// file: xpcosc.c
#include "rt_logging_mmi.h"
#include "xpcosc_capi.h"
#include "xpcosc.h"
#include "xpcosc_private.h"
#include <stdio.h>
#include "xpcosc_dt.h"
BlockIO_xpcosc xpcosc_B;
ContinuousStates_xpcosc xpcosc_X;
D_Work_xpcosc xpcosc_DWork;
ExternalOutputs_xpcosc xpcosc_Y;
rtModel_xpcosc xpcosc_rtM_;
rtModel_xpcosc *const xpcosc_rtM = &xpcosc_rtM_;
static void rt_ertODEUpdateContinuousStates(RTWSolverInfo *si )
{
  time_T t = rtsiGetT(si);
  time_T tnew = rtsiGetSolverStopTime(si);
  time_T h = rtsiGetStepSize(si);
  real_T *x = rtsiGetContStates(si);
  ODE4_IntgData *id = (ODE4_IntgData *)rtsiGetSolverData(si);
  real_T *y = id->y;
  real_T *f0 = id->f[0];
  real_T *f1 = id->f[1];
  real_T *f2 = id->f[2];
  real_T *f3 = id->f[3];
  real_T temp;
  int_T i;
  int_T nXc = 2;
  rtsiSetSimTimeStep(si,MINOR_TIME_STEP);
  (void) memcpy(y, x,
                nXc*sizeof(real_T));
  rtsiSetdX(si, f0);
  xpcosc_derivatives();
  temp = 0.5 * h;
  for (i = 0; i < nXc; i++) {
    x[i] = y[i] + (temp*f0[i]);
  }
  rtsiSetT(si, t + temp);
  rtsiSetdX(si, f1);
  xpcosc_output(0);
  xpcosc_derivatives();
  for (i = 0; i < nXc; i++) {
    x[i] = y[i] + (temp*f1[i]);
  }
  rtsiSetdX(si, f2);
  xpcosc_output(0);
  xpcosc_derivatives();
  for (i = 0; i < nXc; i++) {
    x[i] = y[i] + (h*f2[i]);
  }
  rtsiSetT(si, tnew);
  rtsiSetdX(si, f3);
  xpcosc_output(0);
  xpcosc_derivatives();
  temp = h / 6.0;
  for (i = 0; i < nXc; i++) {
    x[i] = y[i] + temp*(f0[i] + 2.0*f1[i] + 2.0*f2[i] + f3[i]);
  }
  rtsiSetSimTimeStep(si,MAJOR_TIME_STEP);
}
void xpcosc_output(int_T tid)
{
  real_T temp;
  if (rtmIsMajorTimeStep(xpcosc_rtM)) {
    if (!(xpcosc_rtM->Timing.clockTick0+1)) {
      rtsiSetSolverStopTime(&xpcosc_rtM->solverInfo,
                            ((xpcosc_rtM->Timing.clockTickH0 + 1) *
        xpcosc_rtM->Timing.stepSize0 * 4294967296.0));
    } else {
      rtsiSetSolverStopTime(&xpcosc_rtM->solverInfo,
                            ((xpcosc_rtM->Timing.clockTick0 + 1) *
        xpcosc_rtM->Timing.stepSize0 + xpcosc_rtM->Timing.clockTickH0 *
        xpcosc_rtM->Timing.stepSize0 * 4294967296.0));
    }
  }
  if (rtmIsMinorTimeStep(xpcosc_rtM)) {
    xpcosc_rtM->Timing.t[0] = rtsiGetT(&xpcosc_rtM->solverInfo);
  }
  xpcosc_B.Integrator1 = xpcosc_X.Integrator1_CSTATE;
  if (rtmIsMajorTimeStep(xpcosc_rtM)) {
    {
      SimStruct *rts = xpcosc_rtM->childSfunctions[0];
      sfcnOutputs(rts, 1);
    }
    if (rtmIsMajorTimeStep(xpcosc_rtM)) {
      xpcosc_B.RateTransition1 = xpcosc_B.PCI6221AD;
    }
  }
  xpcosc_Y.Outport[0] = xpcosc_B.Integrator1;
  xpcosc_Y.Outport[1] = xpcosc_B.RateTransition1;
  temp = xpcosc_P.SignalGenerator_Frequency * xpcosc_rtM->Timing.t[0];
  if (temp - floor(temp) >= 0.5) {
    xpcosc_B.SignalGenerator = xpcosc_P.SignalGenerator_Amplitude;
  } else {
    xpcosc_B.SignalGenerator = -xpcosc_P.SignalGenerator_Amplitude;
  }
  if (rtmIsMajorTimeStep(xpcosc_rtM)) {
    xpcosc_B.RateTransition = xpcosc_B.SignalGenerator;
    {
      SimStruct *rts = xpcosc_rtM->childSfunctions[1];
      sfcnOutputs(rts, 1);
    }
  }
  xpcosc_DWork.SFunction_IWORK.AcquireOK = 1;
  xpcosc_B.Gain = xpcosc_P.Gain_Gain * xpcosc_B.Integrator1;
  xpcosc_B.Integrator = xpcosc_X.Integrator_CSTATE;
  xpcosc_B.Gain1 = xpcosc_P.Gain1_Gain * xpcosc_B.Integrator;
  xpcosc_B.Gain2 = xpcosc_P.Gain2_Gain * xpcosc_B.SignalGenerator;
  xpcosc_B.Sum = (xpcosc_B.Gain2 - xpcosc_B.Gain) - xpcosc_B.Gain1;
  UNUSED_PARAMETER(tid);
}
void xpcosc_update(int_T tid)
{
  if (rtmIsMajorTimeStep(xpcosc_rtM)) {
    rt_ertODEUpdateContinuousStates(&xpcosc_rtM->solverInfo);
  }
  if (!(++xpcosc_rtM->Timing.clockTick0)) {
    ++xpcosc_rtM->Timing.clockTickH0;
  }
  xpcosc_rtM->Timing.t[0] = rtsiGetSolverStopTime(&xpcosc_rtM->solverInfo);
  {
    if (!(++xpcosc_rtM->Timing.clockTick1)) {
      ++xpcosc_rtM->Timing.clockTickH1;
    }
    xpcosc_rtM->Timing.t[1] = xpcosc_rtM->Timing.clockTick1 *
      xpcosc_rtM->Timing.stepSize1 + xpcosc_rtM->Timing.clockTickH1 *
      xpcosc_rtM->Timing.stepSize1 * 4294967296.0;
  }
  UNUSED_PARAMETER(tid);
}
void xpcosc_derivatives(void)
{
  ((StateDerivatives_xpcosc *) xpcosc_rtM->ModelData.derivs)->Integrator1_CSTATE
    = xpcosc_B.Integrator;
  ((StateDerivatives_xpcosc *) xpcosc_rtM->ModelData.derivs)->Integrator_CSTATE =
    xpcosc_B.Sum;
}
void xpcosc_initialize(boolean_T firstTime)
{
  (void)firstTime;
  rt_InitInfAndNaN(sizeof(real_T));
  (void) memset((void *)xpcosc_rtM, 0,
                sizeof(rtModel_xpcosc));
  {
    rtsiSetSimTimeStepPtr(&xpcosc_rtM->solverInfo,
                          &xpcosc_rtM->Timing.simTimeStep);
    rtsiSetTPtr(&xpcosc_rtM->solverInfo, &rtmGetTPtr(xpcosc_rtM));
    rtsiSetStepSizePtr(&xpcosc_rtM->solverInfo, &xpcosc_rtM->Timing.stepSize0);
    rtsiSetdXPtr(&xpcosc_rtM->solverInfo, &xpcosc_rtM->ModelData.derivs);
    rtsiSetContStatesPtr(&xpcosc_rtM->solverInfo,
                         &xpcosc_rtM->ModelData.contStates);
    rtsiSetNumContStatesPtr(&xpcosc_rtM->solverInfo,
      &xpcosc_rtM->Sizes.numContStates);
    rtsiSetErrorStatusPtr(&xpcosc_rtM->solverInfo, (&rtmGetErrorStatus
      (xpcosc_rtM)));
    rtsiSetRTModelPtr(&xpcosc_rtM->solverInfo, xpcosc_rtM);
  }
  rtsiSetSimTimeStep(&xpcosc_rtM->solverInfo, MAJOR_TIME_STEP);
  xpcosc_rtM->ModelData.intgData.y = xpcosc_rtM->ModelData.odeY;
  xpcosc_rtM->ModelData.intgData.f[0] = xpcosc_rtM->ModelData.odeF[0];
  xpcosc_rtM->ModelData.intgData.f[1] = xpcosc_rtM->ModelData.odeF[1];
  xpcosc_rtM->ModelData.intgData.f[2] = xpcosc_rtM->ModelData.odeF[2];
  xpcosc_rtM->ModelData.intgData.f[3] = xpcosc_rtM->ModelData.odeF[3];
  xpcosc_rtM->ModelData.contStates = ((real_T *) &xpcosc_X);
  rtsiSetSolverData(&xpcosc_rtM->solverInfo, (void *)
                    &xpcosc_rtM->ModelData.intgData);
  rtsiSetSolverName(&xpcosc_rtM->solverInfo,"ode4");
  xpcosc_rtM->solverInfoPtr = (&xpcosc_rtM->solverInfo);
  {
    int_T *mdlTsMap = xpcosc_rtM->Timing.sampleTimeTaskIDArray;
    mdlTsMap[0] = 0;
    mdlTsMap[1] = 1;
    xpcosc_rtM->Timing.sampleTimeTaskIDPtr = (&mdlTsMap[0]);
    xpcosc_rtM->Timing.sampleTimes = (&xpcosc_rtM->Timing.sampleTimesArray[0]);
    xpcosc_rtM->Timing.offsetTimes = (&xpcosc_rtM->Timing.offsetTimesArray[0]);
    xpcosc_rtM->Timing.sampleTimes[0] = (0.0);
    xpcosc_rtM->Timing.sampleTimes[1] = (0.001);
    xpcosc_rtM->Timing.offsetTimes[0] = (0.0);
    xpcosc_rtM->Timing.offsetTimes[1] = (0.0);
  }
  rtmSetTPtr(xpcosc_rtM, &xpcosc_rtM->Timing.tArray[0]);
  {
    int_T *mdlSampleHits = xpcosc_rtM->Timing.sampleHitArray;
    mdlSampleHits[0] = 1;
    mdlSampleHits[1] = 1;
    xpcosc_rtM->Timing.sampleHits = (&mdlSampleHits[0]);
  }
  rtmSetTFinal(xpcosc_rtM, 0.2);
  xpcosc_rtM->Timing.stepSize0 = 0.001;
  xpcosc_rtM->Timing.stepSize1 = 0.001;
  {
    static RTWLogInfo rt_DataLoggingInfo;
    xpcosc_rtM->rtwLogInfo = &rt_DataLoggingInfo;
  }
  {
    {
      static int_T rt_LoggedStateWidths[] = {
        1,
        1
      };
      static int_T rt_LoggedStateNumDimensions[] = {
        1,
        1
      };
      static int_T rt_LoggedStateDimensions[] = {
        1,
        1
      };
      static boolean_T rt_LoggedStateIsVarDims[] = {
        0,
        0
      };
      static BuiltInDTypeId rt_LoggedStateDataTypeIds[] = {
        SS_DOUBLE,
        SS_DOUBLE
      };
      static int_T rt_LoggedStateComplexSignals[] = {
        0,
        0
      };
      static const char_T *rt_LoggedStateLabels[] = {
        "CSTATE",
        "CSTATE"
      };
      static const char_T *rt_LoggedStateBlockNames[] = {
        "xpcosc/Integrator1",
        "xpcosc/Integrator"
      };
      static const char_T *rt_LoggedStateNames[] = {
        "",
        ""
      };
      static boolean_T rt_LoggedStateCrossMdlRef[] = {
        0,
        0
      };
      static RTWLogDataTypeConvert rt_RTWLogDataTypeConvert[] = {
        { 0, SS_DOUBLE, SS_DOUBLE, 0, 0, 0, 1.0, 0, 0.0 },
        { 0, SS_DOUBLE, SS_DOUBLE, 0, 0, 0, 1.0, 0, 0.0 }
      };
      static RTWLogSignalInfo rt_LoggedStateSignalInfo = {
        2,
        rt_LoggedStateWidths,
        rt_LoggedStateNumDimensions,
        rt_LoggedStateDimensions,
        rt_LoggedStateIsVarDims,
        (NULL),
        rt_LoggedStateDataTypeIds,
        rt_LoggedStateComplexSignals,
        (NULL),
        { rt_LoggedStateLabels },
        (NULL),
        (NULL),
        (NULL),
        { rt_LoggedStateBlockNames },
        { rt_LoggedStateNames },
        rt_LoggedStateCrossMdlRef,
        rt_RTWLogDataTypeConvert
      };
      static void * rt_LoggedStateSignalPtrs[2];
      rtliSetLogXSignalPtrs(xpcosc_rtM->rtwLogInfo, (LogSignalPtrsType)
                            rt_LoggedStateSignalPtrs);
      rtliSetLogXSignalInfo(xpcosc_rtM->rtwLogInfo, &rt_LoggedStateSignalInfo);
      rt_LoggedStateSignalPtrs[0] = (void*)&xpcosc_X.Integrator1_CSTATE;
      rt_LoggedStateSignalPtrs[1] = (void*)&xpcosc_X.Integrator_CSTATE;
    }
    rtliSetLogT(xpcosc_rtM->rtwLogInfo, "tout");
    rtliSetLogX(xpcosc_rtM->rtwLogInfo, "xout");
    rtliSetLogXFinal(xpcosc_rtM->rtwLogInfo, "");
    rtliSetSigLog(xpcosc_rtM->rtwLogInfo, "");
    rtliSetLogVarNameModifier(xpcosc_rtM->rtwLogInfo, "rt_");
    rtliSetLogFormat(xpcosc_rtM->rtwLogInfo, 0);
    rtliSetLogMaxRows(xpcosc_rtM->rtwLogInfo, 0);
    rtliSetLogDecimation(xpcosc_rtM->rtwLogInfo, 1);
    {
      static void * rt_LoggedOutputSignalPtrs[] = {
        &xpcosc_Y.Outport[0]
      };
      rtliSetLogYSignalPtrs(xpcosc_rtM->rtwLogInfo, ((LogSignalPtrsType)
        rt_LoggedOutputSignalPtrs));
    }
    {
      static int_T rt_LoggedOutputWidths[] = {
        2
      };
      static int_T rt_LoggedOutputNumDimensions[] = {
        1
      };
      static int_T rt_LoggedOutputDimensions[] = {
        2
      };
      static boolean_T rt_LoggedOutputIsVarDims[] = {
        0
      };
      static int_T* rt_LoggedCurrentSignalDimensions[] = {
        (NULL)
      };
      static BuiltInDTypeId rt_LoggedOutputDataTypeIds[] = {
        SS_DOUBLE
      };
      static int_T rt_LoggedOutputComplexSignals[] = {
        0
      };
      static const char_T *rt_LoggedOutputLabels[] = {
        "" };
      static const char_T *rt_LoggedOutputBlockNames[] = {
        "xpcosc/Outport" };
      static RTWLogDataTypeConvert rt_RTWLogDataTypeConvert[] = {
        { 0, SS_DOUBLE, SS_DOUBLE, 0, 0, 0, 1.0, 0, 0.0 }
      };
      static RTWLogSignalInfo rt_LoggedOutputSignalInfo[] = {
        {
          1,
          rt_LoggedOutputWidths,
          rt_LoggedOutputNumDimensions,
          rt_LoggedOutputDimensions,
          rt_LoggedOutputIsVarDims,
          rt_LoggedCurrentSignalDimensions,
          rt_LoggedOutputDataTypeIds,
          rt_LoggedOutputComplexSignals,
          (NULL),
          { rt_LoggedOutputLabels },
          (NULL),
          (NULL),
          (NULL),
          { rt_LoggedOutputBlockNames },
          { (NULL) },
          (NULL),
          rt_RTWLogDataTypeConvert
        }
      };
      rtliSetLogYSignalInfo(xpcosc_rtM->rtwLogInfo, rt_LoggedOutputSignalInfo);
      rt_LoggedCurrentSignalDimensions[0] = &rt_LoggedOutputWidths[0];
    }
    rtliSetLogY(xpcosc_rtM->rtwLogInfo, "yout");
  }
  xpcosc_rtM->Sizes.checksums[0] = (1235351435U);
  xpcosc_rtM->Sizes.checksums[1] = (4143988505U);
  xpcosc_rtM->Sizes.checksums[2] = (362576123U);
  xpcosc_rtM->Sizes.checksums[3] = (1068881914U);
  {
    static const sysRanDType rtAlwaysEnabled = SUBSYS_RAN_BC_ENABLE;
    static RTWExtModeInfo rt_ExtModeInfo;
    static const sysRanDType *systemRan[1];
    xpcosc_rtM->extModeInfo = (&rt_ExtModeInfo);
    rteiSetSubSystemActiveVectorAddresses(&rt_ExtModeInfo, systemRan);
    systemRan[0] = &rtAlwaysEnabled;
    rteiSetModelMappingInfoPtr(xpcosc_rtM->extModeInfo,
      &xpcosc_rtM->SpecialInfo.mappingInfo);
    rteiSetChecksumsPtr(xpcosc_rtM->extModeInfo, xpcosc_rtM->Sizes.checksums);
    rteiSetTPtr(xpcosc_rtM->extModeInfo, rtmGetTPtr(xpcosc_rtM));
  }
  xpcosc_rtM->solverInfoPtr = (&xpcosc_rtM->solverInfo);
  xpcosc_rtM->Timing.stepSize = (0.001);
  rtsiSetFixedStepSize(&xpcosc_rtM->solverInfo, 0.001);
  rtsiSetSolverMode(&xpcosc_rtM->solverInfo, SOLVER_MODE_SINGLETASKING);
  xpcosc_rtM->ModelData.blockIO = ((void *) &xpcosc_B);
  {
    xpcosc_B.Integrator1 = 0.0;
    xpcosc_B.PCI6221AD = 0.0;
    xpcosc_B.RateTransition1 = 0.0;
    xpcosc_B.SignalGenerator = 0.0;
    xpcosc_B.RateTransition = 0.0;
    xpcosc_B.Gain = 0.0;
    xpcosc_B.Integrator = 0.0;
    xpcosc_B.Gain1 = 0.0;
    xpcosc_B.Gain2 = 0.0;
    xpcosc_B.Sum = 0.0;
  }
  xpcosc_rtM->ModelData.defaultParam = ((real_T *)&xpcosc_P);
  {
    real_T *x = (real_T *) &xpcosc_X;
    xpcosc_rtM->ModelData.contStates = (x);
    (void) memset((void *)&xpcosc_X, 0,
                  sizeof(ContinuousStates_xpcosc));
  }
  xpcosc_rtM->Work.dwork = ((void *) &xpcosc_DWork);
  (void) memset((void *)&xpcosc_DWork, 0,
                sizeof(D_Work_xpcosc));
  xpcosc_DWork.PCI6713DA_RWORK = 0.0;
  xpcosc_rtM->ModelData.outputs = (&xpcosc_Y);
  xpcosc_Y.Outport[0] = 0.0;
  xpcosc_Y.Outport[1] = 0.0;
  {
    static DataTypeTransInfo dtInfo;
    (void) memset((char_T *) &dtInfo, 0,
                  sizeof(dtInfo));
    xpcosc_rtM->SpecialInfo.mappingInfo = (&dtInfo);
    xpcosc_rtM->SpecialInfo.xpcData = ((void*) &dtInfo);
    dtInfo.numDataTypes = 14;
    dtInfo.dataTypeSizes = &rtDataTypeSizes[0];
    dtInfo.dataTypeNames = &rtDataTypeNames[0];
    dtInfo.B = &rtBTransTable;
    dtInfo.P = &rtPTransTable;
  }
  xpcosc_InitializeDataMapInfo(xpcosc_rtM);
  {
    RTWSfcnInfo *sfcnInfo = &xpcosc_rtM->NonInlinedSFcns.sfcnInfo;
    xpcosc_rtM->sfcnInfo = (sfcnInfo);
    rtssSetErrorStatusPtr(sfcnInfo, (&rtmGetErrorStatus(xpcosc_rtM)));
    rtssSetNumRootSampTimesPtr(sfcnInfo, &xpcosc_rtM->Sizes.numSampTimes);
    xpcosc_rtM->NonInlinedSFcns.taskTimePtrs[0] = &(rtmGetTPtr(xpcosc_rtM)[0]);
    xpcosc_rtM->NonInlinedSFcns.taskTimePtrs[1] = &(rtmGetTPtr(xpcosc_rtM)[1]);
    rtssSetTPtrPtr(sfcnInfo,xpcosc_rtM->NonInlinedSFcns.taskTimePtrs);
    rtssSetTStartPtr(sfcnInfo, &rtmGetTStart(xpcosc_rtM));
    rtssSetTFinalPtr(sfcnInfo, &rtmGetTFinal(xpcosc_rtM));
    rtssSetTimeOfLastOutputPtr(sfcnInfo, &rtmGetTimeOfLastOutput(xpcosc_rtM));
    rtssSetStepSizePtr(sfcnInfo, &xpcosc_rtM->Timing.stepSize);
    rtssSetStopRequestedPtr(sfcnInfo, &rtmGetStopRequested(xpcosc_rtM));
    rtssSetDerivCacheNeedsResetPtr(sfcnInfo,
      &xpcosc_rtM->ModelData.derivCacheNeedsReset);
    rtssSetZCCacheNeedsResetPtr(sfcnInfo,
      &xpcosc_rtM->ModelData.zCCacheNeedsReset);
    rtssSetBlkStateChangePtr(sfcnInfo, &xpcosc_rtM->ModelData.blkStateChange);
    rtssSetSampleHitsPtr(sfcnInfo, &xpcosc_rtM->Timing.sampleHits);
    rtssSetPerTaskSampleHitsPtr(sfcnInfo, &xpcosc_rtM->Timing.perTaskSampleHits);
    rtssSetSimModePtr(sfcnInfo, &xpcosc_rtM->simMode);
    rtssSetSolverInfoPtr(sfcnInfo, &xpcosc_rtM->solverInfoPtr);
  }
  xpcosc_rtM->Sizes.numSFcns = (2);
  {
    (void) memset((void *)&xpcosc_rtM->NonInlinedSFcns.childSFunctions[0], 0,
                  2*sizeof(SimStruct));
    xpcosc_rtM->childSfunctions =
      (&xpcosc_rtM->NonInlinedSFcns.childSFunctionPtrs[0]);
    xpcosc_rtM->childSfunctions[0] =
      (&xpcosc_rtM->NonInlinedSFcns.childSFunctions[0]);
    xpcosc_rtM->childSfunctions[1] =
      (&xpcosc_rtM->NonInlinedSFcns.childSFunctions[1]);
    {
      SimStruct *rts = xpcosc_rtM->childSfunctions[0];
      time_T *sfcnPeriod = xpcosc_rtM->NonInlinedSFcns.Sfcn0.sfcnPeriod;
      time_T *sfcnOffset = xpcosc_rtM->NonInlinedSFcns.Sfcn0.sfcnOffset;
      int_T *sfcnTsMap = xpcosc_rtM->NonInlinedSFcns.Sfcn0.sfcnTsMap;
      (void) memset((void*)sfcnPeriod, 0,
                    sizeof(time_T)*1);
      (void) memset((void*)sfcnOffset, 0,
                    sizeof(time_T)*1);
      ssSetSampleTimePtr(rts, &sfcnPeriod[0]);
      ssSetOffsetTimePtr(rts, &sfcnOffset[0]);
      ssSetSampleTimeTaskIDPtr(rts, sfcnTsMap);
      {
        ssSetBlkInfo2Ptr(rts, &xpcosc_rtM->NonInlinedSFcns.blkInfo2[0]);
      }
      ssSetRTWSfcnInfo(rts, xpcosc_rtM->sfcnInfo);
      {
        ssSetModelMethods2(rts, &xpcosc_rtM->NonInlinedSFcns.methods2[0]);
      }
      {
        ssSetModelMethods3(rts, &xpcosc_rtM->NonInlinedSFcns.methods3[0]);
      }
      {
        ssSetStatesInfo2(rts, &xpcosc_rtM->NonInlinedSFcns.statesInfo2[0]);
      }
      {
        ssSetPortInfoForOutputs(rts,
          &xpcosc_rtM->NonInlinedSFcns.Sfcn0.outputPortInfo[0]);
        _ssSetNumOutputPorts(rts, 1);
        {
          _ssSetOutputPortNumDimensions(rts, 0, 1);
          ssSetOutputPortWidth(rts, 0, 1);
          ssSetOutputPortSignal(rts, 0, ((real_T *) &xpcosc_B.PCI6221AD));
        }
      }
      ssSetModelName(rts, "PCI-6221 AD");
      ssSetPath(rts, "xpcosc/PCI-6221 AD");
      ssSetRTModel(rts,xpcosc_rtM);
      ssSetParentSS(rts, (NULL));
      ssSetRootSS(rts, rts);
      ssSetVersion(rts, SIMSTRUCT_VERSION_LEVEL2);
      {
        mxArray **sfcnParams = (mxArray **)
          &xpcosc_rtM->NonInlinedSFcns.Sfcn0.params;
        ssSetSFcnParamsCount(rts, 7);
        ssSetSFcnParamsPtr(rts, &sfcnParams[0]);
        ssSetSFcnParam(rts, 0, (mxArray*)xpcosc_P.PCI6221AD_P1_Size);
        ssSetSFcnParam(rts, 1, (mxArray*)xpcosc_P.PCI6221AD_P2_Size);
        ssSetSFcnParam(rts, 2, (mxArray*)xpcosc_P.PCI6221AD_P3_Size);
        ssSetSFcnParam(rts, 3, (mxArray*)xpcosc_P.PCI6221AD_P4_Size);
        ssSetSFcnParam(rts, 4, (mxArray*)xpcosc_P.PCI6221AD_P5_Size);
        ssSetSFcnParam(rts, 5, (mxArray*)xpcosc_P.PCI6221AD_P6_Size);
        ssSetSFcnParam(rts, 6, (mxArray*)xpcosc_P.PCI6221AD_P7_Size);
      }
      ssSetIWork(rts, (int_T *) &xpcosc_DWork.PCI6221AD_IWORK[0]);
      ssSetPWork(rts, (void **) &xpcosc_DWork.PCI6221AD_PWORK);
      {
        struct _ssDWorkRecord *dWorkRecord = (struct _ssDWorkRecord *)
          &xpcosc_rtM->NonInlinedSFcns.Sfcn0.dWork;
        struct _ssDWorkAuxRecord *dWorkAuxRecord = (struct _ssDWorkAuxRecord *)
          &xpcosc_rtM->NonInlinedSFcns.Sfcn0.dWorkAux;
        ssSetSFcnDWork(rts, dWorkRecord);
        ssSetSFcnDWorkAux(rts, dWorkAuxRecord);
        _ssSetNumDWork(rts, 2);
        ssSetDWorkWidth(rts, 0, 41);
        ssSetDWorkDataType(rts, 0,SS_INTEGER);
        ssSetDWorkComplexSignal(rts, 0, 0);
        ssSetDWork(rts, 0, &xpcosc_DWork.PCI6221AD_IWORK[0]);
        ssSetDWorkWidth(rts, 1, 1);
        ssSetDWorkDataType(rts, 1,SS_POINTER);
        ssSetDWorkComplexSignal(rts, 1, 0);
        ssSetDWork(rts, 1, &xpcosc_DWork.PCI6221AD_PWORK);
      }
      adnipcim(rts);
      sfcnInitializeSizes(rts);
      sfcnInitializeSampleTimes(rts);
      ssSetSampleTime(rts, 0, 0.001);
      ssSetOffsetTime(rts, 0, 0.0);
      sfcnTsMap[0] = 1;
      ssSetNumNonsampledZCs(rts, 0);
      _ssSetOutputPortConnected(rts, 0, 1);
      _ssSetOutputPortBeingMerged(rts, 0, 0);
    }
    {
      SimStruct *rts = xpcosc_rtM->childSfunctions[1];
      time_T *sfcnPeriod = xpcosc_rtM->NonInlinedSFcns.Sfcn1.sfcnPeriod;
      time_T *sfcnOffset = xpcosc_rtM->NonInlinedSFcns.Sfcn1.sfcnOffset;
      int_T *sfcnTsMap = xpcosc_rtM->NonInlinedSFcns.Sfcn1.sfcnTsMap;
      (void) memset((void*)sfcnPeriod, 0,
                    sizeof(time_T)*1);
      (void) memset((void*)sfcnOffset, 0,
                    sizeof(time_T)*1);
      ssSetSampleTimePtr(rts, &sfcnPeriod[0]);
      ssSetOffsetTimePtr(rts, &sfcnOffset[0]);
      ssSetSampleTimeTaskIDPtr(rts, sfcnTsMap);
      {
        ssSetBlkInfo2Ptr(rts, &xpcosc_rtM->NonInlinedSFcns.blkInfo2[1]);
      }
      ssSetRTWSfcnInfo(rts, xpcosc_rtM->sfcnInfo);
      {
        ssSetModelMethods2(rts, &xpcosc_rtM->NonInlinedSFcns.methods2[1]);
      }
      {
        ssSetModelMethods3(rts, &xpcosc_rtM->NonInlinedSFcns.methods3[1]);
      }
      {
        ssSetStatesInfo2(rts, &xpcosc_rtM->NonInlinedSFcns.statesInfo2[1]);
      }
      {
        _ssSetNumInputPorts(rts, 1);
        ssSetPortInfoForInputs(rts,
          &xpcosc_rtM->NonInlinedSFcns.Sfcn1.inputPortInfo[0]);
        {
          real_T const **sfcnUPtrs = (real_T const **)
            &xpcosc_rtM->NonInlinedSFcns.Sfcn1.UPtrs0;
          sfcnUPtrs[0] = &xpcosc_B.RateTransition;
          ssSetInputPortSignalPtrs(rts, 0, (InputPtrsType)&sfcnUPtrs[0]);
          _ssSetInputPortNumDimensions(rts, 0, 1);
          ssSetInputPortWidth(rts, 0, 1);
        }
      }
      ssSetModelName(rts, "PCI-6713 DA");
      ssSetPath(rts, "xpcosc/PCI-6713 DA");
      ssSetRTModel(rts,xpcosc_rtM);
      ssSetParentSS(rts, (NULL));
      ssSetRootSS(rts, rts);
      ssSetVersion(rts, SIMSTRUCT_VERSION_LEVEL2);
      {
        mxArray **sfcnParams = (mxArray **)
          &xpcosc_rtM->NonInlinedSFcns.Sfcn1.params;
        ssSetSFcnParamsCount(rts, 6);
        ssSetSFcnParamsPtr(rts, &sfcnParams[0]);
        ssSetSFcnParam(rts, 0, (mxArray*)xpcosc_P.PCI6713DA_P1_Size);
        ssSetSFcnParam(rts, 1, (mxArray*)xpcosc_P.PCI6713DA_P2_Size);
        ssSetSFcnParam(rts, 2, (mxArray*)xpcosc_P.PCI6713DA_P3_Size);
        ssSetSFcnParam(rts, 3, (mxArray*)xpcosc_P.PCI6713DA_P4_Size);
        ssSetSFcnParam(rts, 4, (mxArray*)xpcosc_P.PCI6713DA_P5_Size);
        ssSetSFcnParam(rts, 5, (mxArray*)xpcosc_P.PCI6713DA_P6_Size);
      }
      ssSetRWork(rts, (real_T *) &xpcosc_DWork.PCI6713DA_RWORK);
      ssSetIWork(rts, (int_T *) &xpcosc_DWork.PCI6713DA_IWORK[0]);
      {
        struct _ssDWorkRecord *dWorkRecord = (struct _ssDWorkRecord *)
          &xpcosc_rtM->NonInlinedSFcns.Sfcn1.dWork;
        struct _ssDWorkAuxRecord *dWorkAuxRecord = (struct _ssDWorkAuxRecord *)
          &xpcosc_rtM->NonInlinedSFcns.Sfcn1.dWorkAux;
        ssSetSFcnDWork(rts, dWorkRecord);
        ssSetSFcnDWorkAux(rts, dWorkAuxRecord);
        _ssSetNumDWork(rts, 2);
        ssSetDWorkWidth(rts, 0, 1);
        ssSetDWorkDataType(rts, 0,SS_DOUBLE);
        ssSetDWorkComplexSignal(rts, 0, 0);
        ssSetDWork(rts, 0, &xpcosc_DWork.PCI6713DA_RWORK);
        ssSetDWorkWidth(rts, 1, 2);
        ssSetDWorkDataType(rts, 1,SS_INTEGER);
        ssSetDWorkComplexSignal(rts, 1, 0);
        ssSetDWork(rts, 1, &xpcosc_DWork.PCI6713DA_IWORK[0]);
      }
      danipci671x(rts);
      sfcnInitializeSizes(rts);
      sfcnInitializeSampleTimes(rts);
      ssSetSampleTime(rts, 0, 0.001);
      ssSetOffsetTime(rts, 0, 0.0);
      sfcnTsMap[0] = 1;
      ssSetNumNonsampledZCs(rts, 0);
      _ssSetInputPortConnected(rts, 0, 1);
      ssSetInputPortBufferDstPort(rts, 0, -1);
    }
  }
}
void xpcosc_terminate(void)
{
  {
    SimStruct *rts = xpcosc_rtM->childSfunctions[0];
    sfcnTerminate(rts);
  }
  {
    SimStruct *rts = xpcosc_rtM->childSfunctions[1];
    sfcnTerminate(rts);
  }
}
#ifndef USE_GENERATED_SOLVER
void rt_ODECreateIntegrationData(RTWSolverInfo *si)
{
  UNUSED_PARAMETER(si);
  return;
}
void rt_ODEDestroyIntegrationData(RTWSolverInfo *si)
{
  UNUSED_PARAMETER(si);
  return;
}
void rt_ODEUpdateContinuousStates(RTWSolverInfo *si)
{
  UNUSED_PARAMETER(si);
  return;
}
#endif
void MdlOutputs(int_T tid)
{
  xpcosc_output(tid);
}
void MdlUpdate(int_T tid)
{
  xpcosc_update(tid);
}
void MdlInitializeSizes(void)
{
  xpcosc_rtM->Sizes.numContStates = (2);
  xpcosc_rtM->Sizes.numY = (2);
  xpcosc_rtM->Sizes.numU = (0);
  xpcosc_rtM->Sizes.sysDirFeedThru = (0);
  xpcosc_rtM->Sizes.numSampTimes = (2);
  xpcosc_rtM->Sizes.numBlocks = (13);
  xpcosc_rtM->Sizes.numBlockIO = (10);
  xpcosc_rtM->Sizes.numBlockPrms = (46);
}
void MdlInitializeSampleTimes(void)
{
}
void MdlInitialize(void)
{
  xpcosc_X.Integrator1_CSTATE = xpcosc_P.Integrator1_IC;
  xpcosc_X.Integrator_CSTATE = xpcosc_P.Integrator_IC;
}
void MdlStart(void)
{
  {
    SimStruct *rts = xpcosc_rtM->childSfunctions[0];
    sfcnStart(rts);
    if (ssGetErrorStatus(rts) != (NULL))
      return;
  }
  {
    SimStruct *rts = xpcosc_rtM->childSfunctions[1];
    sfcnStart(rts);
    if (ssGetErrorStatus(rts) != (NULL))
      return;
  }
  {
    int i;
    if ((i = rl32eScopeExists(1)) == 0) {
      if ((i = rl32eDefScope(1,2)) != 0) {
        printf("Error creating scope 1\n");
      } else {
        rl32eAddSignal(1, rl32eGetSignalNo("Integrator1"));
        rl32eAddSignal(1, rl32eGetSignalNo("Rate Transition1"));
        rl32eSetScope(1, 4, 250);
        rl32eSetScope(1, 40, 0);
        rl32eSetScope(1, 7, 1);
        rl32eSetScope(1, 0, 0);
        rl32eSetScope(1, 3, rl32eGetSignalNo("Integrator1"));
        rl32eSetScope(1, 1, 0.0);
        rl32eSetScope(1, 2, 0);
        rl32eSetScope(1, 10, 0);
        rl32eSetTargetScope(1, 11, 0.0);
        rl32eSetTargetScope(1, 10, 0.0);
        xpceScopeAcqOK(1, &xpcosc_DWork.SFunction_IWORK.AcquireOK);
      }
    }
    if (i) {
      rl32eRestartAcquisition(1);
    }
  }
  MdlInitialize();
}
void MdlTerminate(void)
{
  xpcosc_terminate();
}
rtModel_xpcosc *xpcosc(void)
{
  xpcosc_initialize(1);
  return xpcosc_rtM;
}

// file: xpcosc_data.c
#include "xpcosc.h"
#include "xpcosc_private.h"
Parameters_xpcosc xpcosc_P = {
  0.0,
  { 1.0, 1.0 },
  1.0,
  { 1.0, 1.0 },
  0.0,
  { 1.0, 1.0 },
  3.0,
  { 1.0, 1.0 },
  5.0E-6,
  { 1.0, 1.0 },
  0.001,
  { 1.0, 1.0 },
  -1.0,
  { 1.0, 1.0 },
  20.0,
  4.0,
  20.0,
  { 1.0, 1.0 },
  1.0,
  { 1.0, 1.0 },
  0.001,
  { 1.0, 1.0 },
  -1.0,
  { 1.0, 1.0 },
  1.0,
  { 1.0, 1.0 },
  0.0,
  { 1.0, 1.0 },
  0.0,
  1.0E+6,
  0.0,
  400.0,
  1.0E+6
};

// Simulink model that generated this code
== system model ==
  Outport : Outport  InitialOutput=0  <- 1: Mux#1
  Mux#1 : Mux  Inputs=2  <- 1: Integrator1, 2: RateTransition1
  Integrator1 : Integrator  <- 1: Integrator
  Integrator : Integrator  <- 1: Sum
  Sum : Sum  Inputs=-+-  <- 1: Gain, 2: Gain2, 3: Gain1
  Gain : Gain  Gain=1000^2  <- 1: Integrator1
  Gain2 : Gain  Gain=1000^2  <- 1: SignalGenerator
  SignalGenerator : SignalGenerator  Amplitude=4  Frequency=20
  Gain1 : Gain  Gain=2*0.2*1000  <- 1: Integrator
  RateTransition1 : RateTransition  <- 1: PCI6221AD
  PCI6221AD : S-Function  FunctionName=adnipcim
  ScopexPC#1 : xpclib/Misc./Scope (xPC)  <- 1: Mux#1
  PCI6713DA : xpcnilib/D//A/PCI-6713 DA  <- 1: RateTransition
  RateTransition : RateTransition  <- 1: SignalGenerator
